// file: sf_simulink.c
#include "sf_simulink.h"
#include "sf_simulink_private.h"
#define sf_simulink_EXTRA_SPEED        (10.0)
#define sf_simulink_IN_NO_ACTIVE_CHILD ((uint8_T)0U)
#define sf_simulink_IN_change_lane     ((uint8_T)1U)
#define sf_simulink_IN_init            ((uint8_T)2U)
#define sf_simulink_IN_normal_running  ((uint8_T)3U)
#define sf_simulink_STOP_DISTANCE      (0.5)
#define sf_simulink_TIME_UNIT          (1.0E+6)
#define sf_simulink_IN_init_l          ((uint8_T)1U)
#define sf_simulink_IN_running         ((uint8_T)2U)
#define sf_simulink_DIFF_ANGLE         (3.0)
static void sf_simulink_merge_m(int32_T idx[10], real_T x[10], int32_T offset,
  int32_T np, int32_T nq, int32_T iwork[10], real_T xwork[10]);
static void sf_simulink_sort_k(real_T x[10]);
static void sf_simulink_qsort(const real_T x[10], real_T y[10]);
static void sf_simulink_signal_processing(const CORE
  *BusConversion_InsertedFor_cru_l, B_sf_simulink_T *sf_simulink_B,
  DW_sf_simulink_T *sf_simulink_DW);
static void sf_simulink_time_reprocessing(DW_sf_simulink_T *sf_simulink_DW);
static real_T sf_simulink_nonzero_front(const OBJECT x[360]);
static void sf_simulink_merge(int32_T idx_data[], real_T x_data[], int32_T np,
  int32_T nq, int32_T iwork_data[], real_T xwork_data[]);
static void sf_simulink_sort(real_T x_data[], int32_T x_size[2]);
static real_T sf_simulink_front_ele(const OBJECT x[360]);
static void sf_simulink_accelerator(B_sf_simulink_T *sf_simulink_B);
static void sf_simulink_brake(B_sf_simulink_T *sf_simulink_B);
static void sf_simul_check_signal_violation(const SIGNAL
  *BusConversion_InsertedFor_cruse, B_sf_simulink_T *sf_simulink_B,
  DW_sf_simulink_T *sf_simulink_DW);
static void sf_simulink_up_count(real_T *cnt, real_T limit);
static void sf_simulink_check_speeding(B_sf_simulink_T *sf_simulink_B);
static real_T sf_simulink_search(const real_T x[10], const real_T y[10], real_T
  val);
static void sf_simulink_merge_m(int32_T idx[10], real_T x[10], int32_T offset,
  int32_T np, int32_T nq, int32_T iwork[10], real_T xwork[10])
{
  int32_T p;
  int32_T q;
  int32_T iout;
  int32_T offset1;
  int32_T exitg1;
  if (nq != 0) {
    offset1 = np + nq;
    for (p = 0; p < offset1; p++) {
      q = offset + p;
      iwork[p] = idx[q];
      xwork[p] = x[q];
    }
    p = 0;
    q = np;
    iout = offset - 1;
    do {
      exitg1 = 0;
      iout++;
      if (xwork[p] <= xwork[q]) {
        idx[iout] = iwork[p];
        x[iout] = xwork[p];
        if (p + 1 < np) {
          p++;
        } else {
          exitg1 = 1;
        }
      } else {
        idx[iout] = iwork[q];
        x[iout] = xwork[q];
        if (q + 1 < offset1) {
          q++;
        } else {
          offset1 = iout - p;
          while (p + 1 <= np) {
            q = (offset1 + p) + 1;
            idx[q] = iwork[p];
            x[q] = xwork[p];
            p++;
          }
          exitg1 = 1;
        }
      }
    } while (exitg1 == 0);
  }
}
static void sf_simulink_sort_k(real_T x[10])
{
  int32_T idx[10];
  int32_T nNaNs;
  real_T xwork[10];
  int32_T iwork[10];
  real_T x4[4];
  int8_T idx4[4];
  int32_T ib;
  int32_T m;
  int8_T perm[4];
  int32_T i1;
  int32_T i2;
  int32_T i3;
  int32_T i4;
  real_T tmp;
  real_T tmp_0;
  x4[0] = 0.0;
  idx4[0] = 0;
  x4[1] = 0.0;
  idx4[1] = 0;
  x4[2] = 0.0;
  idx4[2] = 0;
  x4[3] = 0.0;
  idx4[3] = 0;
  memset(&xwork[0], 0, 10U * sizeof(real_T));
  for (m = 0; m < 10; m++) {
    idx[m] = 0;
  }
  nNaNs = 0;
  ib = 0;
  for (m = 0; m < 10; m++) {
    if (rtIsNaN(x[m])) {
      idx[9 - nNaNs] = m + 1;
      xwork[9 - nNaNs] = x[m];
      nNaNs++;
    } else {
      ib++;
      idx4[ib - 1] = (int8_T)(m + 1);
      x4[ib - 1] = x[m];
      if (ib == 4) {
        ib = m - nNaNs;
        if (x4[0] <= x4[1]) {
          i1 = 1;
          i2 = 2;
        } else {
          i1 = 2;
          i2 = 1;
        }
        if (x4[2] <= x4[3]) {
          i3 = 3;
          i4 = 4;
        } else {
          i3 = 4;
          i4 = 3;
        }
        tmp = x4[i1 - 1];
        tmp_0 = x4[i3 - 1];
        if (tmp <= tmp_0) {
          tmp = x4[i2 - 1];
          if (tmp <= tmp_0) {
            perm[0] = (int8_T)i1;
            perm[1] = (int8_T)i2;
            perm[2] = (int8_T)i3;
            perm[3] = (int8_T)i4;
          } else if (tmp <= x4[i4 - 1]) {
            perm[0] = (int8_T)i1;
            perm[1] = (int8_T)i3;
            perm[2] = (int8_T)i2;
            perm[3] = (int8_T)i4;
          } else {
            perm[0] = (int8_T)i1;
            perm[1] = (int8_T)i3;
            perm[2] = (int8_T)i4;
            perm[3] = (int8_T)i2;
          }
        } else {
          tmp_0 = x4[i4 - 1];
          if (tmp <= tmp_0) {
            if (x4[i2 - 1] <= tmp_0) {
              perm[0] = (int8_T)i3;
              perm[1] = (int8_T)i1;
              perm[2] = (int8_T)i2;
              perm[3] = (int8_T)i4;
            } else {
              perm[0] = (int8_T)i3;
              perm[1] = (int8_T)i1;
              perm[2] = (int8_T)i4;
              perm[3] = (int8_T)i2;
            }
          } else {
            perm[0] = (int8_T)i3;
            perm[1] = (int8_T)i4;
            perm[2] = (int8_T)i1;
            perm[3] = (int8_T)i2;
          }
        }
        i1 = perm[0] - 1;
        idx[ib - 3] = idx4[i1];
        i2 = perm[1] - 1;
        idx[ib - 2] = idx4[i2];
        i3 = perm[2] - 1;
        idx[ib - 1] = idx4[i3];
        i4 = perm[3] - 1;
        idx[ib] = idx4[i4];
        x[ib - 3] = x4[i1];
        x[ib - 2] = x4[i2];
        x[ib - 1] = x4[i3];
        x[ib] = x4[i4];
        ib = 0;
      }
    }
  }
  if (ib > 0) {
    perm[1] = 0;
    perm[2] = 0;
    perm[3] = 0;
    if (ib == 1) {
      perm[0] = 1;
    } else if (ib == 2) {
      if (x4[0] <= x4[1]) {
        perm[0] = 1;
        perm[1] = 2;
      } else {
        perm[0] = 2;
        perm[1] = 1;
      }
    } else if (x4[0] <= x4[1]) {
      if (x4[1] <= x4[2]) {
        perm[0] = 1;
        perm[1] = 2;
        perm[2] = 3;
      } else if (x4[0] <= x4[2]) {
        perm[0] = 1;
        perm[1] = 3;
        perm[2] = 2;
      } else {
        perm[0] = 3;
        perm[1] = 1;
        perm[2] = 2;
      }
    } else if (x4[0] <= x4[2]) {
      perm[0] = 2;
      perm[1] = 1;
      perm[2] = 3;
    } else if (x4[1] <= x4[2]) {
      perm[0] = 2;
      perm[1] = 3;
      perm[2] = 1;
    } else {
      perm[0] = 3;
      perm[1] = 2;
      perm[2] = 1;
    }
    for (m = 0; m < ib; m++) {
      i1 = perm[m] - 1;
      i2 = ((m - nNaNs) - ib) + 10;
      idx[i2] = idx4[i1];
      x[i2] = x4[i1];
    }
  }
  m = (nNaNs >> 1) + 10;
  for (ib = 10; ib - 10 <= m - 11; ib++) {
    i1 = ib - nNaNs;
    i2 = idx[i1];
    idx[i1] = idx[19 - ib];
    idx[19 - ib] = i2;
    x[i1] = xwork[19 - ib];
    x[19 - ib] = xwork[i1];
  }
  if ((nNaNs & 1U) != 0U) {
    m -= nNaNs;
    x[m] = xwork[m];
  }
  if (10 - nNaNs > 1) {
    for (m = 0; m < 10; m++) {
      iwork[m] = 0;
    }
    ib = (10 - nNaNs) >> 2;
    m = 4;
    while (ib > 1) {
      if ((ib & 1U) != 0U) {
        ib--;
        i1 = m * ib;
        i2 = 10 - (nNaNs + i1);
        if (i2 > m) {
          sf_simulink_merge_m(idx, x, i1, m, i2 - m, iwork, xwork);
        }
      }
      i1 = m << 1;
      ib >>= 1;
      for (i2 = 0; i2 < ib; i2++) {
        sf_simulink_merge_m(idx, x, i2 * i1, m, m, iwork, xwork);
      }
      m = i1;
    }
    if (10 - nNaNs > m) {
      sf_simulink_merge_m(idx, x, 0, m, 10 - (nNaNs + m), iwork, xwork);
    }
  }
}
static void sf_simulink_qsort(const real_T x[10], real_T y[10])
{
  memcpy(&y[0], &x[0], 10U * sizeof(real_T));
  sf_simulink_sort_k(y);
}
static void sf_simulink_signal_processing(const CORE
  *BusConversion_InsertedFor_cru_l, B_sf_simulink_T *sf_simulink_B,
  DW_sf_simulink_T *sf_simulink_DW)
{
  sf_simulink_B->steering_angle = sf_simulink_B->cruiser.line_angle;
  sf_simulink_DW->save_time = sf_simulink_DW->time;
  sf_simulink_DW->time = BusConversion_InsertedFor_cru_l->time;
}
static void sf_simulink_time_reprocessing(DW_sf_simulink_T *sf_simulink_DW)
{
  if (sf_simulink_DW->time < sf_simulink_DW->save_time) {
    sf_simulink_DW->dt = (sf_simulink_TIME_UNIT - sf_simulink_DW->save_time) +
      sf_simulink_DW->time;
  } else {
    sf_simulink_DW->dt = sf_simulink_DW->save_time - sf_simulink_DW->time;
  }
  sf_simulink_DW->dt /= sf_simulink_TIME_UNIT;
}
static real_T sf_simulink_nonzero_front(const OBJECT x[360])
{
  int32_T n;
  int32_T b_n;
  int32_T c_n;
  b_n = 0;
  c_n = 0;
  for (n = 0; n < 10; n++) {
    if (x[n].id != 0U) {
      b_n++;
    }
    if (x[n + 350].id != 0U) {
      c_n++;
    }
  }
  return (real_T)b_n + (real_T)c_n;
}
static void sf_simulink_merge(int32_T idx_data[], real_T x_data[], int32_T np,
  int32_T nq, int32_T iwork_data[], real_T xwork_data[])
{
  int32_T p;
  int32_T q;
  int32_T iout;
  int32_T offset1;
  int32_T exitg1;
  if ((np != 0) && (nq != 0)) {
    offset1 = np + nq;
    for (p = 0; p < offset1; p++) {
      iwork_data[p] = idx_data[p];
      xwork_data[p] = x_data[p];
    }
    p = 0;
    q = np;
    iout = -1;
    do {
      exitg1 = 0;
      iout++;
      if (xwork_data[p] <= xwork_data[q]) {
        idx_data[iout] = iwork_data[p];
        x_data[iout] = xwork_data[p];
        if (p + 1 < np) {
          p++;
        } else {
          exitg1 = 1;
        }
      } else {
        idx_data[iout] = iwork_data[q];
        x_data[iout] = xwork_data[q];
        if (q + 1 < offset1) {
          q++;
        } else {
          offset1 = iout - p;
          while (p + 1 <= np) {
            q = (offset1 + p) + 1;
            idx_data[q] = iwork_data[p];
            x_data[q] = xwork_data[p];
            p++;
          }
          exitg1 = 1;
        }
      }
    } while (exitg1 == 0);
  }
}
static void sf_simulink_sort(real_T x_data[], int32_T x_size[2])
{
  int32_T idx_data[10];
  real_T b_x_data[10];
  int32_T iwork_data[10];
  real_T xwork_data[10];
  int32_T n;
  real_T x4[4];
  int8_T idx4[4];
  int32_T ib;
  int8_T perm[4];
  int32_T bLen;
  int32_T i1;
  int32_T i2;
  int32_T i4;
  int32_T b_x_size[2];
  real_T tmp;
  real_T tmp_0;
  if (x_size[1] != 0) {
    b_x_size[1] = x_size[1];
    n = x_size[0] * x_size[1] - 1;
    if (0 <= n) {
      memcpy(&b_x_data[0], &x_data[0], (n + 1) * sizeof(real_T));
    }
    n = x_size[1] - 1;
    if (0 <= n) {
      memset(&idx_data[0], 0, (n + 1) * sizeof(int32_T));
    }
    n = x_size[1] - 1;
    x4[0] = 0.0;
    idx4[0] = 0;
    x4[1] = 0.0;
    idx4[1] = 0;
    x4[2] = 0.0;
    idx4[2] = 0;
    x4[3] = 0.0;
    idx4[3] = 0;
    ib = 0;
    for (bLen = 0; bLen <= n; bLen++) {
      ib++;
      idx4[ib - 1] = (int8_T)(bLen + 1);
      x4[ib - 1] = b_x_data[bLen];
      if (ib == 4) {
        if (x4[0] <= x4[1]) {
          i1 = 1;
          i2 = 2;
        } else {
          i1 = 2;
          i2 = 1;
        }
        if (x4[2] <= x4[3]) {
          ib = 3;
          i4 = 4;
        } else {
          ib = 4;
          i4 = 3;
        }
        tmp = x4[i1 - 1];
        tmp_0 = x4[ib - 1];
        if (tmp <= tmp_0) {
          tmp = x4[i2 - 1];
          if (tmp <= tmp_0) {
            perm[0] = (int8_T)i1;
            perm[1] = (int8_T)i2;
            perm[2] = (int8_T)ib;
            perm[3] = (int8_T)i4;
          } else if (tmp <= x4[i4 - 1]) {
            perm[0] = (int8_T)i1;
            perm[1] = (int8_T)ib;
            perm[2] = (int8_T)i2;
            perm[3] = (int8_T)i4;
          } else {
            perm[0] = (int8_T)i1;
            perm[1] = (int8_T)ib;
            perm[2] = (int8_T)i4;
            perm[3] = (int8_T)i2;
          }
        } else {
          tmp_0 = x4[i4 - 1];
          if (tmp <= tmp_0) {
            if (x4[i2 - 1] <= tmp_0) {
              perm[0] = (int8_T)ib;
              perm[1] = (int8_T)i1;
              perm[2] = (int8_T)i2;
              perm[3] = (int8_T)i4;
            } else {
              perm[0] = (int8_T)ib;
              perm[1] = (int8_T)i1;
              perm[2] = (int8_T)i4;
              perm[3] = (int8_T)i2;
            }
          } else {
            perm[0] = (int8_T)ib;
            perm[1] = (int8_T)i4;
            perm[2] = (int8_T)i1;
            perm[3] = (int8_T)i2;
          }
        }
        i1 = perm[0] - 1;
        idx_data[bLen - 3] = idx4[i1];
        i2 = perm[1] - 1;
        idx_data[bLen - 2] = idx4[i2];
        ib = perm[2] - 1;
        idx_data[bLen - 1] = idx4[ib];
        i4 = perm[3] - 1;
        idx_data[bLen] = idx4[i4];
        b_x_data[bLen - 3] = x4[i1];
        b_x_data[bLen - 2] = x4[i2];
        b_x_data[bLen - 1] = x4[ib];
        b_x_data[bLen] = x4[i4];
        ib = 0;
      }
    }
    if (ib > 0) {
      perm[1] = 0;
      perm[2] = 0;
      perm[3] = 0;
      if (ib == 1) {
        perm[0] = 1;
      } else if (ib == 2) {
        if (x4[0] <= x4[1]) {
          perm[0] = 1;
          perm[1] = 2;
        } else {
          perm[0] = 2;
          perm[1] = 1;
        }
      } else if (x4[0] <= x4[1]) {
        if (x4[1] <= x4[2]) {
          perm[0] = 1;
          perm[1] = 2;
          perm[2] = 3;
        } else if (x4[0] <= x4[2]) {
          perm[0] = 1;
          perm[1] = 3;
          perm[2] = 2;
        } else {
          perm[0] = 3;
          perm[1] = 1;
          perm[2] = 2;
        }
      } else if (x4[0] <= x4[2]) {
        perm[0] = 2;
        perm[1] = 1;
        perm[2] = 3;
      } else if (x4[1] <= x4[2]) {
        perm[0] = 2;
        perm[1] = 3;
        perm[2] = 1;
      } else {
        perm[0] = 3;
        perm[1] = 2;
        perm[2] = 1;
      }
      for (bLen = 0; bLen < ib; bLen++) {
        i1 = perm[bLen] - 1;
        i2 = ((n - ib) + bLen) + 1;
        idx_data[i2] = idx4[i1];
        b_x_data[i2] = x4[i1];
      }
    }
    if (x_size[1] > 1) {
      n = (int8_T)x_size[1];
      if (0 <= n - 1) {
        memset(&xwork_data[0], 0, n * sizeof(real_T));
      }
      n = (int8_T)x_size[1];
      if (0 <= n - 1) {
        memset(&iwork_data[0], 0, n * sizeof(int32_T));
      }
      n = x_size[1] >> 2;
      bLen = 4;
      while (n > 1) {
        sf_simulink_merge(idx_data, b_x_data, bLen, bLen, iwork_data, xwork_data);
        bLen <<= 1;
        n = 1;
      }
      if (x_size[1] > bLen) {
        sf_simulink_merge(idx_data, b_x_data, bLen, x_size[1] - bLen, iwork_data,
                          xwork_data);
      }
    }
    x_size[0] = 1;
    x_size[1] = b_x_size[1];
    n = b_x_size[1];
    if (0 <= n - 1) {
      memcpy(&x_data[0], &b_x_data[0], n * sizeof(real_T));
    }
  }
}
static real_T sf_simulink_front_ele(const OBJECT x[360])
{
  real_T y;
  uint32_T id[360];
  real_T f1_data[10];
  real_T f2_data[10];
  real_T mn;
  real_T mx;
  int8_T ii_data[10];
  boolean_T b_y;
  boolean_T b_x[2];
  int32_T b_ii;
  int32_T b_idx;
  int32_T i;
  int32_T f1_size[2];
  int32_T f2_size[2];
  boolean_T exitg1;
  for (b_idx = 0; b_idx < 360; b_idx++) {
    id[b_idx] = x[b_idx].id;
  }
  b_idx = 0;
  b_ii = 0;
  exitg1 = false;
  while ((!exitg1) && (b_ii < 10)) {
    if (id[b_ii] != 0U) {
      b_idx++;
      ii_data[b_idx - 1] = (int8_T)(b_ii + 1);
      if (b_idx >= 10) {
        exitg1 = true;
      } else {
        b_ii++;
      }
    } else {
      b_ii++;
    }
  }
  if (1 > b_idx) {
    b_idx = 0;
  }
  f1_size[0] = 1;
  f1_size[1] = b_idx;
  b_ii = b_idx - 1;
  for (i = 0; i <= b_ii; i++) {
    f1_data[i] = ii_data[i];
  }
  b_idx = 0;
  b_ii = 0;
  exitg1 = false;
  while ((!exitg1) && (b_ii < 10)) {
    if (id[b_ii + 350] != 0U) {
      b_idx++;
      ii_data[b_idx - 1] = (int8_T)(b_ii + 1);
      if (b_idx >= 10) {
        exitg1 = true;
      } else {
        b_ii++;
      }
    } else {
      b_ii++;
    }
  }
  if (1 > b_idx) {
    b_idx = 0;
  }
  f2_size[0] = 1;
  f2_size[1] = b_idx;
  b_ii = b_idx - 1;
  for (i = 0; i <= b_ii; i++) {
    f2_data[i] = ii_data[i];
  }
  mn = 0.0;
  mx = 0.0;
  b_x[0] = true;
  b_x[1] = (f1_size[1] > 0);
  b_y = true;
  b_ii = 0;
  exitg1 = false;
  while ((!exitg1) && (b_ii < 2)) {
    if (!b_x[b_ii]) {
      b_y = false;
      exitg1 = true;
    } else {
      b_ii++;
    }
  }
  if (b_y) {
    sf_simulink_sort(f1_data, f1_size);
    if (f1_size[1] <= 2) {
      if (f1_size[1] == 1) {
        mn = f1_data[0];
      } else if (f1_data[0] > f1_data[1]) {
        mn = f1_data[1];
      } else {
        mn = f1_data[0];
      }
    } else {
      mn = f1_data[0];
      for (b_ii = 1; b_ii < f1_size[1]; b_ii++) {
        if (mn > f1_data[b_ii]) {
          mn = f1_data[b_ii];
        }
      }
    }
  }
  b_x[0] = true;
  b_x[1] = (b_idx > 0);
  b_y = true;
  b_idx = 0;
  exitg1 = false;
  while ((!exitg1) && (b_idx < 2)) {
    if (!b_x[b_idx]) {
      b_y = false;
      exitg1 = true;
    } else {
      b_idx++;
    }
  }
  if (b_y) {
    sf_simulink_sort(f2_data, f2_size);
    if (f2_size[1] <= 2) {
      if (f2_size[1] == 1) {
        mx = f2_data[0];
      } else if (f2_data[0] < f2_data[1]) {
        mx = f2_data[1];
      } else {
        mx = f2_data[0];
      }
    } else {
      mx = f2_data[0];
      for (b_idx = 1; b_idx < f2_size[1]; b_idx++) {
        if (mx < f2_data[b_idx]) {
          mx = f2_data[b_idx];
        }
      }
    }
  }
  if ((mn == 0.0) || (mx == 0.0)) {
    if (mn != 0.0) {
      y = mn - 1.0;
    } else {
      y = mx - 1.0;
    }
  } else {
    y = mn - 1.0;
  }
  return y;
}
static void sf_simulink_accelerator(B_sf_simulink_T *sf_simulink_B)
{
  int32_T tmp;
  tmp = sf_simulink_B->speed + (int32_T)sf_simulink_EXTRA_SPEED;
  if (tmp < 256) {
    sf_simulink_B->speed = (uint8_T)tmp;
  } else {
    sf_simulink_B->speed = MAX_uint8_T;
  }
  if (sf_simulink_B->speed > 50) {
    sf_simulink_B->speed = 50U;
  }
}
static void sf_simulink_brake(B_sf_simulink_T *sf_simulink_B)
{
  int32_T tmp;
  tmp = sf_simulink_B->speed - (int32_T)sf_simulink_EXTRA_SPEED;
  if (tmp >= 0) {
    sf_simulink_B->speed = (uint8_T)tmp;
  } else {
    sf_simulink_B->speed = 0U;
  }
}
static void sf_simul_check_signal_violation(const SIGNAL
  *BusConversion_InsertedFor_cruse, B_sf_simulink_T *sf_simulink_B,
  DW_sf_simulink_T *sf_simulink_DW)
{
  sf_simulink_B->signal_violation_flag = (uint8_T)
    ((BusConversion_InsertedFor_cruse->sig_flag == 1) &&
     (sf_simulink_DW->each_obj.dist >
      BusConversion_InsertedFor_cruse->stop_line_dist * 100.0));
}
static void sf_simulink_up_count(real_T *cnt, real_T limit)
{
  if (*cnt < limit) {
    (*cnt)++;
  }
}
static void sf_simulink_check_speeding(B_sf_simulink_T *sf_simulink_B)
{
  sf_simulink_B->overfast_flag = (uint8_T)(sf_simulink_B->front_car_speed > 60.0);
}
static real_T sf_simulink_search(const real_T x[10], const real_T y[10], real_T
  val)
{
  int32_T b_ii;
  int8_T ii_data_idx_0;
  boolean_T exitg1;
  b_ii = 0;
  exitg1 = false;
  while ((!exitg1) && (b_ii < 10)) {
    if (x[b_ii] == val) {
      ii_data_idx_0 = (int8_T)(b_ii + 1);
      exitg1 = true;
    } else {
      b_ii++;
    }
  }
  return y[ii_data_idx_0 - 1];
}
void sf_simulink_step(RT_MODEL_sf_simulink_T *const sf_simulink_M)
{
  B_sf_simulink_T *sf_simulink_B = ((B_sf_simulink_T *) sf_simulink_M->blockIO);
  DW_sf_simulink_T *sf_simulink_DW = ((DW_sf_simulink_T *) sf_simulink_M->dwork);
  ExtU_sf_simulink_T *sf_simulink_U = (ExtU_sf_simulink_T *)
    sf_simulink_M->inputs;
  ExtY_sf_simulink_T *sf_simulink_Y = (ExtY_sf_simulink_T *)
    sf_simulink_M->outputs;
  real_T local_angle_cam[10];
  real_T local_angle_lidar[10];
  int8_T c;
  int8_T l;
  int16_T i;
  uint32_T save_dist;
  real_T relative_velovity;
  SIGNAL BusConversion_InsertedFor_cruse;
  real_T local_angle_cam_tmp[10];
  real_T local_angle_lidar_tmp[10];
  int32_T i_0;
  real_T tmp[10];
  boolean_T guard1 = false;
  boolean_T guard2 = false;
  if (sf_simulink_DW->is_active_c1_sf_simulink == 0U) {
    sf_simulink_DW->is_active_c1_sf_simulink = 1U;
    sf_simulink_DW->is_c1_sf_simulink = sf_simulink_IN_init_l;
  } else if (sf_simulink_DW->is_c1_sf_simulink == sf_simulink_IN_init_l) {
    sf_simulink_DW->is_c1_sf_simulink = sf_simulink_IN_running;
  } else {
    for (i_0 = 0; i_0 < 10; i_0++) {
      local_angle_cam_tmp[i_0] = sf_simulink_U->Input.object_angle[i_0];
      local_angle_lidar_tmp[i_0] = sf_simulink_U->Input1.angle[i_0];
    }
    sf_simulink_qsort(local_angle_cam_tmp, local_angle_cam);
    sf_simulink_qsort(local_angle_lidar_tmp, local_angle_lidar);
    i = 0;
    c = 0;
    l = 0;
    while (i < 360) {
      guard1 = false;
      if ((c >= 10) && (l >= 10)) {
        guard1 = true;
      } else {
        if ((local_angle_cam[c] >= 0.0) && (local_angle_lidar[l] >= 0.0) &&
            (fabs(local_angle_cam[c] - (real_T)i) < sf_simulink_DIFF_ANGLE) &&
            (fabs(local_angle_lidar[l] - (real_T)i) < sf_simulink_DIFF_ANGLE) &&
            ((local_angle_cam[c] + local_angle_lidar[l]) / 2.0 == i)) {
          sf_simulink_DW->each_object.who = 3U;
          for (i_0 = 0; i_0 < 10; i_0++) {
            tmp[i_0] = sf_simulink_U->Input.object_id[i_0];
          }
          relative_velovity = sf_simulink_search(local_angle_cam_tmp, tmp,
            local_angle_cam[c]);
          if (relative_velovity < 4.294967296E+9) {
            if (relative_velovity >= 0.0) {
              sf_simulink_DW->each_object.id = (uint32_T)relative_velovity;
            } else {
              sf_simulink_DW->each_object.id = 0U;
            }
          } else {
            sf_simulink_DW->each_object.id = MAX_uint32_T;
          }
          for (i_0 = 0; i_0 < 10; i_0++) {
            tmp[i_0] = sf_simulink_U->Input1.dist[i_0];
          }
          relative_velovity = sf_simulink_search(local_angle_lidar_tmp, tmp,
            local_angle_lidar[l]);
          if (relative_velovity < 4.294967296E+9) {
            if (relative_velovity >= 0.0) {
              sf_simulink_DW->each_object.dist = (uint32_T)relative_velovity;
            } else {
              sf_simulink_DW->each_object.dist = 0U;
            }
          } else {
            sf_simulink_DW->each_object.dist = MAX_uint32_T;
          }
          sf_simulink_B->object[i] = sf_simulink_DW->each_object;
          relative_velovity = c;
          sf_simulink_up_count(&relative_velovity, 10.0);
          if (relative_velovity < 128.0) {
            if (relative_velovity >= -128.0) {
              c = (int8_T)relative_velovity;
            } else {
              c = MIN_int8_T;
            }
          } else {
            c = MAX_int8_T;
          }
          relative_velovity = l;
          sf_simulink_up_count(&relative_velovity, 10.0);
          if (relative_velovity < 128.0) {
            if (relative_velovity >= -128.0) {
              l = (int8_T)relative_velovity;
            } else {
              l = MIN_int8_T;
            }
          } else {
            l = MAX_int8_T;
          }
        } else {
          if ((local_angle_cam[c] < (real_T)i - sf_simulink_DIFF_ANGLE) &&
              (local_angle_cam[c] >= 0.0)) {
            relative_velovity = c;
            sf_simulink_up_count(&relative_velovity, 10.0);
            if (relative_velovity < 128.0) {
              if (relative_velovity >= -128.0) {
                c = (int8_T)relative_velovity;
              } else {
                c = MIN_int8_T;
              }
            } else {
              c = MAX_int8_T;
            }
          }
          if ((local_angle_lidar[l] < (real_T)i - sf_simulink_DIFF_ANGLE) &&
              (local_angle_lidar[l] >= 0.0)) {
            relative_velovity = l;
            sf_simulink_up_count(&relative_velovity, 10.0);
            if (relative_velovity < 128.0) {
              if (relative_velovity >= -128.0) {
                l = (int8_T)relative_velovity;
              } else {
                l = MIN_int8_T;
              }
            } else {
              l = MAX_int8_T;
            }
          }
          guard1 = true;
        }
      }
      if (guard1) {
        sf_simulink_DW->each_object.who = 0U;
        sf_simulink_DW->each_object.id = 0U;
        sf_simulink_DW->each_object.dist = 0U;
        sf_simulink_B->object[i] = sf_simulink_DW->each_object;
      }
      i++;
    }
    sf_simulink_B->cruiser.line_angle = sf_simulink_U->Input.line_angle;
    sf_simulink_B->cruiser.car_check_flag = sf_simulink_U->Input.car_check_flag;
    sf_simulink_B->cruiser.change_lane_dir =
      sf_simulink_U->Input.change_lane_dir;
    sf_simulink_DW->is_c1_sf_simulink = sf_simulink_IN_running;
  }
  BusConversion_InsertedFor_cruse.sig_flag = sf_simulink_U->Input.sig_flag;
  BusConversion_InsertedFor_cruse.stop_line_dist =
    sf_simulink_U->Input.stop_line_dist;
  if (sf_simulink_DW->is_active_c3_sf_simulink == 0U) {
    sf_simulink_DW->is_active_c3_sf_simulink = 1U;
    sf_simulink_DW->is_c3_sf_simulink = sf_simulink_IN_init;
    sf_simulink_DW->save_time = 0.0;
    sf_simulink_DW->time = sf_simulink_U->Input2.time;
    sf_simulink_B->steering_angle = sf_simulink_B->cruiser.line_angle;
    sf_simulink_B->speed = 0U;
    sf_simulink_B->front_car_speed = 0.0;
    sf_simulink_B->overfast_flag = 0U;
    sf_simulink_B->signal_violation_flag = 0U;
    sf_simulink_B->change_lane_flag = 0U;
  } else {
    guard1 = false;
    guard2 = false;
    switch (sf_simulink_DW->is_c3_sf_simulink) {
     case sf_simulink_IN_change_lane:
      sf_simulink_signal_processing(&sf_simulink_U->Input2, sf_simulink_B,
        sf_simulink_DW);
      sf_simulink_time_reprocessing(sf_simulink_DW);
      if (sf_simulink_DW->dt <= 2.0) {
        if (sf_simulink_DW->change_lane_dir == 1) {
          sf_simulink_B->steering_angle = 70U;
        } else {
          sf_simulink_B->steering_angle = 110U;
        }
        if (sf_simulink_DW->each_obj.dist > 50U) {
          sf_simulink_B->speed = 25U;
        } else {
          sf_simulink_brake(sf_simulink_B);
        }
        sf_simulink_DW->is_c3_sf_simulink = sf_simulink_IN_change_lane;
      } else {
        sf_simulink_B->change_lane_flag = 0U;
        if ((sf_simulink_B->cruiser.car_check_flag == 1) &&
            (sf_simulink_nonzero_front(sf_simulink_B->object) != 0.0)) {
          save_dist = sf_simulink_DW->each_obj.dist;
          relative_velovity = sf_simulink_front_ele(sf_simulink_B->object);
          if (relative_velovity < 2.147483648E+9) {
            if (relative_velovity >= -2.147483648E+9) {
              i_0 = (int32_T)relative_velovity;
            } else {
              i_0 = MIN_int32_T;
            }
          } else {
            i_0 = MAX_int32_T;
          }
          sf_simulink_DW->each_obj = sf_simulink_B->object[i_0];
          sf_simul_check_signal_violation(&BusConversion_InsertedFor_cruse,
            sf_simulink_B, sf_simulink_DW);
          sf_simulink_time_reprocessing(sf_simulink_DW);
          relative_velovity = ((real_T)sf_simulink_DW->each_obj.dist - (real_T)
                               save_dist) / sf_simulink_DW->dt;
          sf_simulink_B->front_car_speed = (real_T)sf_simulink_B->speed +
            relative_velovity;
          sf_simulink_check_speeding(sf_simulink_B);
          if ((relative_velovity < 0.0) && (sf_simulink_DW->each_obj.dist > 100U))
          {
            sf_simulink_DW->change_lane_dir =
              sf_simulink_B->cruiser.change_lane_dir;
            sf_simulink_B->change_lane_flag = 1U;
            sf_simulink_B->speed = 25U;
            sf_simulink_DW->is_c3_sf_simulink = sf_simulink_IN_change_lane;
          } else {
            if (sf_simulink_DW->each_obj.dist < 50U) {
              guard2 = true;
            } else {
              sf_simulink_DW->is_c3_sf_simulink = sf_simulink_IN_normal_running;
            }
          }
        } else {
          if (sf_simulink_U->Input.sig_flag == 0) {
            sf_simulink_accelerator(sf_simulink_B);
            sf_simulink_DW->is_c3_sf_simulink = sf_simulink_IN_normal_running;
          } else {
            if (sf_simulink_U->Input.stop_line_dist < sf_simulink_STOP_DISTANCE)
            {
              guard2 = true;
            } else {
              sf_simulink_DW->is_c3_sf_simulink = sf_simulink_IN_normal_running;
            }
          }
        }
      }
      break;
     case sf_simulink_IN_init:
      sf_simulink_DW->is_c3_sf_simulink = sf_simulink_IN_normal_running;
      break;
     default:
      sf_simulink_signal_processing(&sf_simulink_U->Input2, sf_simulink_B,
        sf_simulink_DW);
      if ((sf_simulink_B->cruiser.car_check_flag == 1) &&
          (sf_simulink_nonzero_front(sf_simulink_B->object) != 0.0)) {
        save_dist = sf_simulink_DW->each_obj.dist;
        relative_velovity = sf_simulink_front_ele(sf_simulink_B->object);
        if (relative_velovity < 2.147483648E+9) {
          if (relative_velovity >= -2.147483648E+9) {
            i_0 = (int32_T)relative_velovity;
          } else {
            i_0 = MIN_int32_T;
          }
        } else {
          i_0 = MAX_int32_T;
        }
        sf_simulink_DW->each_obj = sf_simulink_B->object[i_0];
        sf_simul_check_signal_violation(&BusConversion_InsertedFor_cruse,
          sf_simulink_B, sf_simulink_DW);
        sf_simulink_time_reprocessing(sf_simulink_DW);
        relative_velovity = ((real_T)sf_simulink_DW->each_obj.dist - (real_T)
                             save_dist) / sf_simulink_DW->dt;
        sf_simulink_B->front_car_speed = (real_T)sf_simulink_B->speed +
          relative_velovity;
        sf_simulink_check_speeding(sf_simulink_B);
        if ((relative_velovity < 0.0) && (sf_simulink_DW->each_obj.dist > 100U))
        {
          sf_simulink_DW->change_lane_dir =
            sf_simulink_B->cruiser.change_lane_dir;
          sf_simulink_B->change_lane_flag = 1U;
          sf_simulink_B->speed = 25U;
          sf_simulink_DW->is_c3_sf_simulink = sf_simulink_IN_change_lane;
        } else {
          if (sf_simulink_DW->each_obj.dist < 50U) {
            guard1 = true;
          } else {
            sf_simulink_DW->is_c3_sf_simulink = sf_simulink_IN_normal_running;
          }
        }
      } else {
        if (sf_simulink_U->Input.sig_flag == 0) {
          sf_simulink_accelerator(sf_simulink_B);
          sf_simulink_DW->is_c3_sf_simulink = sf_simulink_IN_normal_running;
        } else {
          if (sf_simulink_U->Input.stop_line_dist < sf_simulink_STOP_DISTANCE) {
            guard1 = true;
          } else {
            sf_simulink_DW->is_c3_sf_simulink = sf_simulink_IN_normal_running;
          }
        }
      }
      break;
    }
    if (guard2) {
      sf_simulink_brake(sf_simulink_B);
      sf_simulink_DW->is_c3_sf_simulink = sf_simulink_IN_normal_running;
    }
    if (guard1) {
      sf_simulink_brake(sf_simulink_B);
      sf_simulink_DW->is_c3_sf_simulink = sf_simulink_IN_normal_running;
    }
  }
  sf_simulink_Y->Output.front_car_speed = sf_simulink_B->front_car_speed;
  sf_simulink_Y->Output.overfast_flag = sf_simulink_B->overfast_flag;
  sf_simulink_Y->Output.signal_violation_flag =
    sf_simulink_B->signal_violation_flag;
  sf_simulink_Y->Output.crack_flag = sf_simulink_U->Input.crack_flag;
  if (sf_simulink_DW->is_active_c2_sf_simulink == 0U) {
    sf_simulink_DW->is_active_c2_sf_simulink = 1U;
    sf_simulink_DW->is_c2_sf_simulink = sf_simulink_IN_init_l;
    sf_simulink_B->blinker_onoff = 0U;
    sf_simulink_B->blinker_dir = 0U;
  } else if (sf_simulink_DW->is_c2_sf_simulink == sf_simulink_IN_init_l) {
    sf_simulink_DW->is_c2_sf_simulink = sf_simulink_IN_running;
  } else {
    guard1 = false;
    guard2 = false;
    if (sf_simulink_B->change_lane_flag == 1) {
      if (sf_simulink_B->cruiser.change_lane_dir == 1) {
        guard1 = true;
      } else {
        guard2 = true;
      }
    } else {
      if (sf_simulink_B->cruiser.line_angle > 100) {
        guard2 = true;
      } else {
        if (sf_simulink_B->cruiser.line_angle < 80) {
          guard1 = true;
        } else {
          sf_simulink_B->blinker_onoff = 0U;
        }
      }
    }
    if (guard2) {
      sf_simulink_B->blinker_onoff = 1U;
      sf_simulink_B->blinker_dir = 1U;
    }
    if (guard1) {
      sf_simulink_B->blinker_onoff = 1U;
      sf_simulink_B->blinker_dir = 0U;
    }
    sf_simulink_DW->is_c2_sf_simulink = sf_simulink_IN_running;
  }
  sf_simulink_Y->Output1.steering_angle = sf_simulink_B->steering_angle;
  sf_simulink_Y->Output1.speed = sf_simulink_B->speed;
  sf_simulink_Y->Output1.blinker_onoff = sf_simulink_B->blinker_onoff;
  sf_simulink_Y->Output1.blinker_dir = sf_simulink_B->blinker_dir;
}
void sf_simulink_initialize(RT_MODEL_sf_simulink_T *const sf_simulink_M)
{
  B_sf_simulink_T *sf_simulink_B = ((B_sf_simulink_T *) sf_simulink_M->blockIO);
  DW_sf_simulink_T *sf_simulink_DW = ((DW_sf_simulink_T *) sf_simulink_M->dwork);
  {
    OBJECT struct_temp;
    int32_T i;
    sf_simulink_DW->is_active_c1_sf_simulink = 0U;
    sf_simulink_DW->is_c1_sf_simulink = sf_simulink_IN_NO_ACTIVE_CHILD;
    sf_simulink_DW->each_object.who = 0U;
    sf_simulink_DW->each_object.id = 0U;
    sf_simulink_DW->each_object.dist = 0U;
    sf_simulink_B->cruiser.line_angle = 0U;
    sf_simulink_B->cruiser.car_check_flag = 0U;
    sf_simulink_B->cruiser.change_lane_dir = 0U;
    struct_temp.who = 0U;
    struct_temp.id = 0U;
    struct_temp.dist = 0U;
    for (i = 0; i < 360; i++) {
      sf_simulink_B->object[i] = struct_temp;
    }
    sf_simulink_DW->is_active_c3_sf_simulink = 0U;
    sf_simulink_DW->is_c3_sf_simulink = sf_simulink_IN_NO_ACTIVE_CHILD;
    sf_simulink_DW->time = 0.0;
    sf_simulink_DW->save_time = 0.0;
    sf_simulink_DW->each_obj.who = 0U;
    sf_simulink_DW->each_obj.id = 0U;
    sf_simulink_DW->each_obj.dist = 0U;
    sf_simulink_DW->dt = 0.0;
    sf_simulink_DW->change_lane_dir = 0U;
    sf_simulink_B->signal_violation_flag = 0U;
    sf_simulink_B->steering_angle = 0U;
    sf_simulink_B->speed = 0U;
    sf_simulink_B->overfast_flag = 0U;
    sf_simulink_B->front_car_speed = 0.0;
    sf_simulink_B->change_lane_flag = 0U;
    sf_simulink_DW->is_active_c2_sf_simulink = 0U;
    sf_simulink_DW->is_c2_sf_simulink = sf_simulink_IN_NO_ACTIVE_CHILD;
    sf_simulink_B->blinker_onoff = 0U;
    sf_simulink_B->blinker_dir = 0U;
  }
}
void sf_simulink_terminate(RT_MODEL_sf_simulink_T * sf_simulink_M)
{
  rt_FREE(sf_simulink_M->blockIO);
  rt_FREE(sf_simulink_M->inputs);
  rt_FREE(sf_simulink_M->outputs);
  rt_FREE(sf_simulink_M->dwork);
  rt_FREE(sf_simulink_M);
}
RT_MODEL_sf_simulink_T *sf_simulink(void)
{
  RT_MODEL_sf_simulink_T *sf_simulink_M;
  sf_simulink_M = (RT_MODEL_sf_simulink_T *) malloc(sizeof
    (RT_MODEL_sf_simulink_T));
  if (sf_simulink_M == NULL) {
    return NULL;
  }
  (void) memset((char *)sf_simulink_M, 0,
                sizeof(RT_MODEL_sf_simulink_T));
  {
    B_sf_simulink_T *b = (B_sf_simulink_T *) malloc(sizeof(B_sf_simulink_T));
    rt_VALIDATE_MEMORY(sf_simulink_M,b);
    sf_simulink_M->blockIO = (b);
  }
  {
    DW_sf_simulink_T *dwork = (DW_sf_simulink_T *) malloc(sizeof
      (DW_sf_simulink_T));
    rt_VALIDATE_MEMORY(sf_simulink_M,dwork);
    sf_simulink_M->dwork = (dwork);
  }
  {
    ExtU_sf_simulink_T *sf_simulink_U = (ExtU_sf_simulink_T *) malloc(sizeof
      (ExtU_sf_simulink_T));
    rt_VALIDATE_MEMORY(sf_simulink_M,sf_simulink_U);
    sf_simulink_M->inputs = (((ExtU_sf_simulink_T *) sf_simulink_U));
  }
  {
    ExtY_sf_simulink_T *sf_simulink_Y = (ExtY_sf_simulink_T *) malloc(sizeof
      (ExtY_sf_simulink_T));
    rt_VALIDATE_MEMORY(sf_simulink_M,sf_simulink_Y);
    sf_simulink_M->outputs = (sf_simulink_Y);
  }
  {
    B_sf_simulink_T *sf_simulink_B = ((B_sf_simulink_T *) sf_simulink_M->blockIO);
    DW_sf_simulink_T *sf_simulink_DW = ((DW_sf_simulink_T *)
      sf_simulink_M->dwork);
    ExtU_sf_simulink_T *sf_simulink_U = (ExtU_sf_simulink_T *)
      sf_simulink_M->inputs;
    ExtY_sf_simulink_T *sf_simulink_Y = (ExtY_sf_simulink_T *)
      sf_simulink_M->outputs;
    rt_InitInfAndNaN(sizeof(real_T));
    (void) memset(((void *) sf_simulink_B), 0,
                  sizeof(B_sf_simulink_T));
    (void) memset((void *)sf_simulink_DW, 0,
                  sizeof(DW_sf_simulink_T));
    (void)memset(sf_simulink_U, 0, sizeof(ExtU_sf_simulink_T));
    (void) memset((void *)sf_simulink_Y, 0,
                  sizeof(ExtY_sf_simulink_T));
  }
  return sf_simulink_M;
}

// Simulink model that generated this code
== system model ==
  Input : Inport
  Input1 : Inport
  Input2 : Inport
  Output : Outport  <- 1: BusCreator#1
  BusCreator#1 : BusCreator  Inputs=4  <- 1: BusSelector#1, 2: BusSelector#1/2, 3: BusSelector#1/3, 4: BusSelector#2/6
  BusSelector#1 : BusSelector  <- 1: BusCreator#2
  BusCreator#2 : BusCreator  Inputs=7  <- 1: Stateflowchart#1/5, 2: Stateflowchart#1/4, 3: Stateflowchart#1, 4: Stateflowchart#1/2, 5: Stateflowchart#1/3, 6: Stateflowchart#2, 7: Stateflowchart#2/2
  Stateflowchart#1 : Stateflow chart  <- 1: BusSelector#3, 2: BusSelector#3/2, 3: Input2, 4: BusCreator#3
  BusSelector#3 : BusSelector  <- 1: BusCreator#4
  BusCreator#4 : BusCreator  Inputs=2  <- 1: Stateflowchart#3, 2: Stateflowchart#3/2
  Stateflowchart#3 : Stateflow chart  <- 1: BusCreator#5, 2: Input1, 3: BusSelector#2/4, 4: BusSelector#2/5
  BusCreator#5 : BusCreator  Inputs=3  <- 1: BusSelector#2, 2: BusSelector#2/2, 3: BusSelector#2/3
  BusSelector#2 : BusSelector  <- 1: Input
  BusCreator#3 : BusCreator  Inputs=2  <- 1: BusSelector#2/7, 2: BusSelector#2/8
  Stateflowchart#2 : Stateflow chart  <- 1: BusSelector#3, 2: Stateflowchart#1/6
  Output1 : Outport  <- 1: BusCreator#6
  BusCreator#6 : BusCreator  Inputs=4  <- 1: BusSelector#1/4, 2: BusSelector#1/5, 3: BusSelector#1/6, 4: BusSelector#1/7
== stateflow chart Stateflowchart#3 ==
  state cnt = up_count(cnt, limit) [function]
    (default) -> (junction 136)
    (junction 136) -> (junction 125) [order 1] : [cnt < limit]
        | {cnt = cnt + 1;}
    (junction 131) -> (junction 125)
    (junction 125) -> (junction 133)
    (junction 136) -> (junction 131) [order 2]
  state init
    local_angle_cam = -1;
    local_angle_lidar = -1;
  state running
  (default) -> init
  init -> running
  (junction 99) -> running
  (junction 95) -> (junction 99)
  running -> (junction 180) : /* local data qsort */
      | {
      | local_angle_cam = qsort(cam.object_angle);
      | local_angle_lidar = qsort(lidar.angle);
      | }
  (junction 180) -> (junction 37) : {i = 0; c = 0; l = 0;}
  (junction 227) -> (junction 36) [order 2]
  (junction 36) -> (junction 105) [order 1] : /* each data is bigger than zero,
      | the absolute value of diff between local angles is smaller than three.
      | !!! used data is set minus one !!!
      | data is existed, what... */
      | [
      | local_angle_cam[c] >= 0 && local_angle_lidar[l] >= 0 && ...
      | abs(local_angle_cam[c] - i) < DIFF_ANGLE && ...
      | abs(local_angle_lidar[l] - i) < DIFF_ANGLE && ...
      | (local_angle_cam[c] + local_angle_lidar[l]) / 2 == i
      | ]
  (junction 37) -> (junction 227) [order 1] : [i < 360]
  (junction 227) -> (junction 232) [order 1] : [c >= 10 && l >= 10]
  (junction 36) -> (junction 196) [order 2]
  (junction 105) -> (junction 143) : {
      | each_object.who = 3;
      | each_object.id = search(cam.object_angle, cam.object_id, local_angle_cam[c]);
      | each_object.dist = search(lidar.angle, lidar.dist, local_angle_lidar[l]);
      | object[i] = each_object;
      |
      | c = up_count(c, 10);
      | l = up_count(l, 10);
      | }
  (junction 39) -> (junction 37)
  (junction 37) -> (junction 40) [order 2] : /* data fetch*/
      | {
      | cruiser.line_angle = line_angle;
      | cruiser.car_check_flag = car_check_flag;
      | cruiser.change_lane_dir = cam.change_lane_dir;
      | }
  (junction 196) -> (junction 241) [order 1] : [local_angle_cam[c] < i - DIFF_ANGLE && local_angle_cam[c] >= 0]
      | {c = up_count(c, 10);}
  (junction 196) -> (junction 239) [order 2]
  (junction 241) -> (junction 203)
  (junction 203) -> (junction 239)
  (junction 239) -> (junction 207)
  (junction 207) -> (junction 236) [order 1] : [local_angle_lidar[l] < i - DIFF_ANGLE && local_angle_lidar[l] >= 0]
      | {l = up_count(l, 10);}
  (junction 207) -> (junction 232) [order 2]
  (junction 236) -> (junction 205)
  (junction 205) -> (junction 232)
  (junction 232) -> (junction 38) : {
      | each_object.who = 0;
      | each_object.id = 0;
      | each_object.dist = 0;
      | object[i] = each_object;
      | }
  (junction 40) -> (junction 95)
  (junction 38) -> (junction 39) : {i = i + 1;}
  (junction 143) -> (junction 38)
  data: cnt function_input double; limit function_input double; cnt function_output double; x function_input double size=10; y function_output double size=10; x function_input double size=10; y function_input double size=10; ret function_output double; val function_input double; cam input Bus: C_BUS; lidar input Bus: LIDAR; cruiser output Bus: CRUISER size=1; line_angle input; local_angle_cam local double size=10; local_angle_lidar local double size=10; car_check_flag input; c local int8; l local int8; i local int16; object output Bus: OBJECT size=360; each_object local Bus: OBJECT; DIFF_ANGLE constant double =3
  function y = qsort(x):
    | function y = qsort(x)
    | input = zeros(1,10);
    | for n = 1:10
    |     input(n) = x(n);
    | end
    | input = sort(input);
    | for n = 1:10
    |     y(n) = input(n);
    | end
  function ret = search(x, y, val):
    | function ret = search(x, y, val)
    | ind = find(x == val, 1);
    | ret = y(ind(1));

== stateflow chart Stateflowchart#2 ==
  state init
    blinker_onoff = 0;
    blinker_dir = 0;
  state running
  (default) -> init
  init -> running
  (junction 32) -> running
  (junction 30) -> (junction 32)
  running -> (junction 17)
  (junction 17) -> (junction 19) [order 1] : /* lane change or not */
      | [change_lane_flag == 1]
  (junction 19) -> (junction 41) [order 1] : [cruiser.change_lane_dir == 1]
  (junction 17) -> (junction 21) [order 2]
  (junction 19) -> (junction 45) [order 2]
  (junction 41) -> (junction 46)
  (junction 21) -> (junction 45) [order 1] : /* turn left */
      | [cruiser.line_angle > ANGLE_STD + 10]
  (junction 21) -> (junction 35) [order 2]
  (junction 45) -> (junction 49) : {blinker_onoff = 1;
      | blinker_dir = 1;}
  (junction 35) -> (junction 46) [order 1] : /* turn right */
      | [cruiser.line_angle < ANGLE_STD - 10]
  (junction 35) -> (junction 28) [order 2] : {blinker_onoff = 0;}
  (junction 46) -> (junction 38) : {blinker_onoff = 1;
      | blinker_dir = 0;}
  (junction 28) -> (junction 30)
  (junction 49) -> (junction 28)
  (junction 38) -> (junction 49)
  data: cruiser input Bus: CRUISER; blinker_onoff output uint8; blinker_dir output uint8; change_lane_flag input; ANGLE_STD constant double =90

== stateflow chart Stateflowchart#1 ==
  state signal_processing [function]
    (default) -> (junction 977)
    (junction 977) -> (junction 965) [order 1] : % yellow or red signal
        | [signal.sig_flag == 1]
    (junction 977) -> (junction 969) [order 2]
    (junction 965) -> (junction 969) [order 2]
    (junction 969) -> (junction 971) : {move_f = 1;}
    (junction 965) -> (junction 970) [order 1] : [signal.stop_line_dist < STOP_DISTANCE]
        | {move_f = 0;}
    (junction 970) -> (junction 971)
    (junction 971) -> (junction 966) : {
        | steering_angle = cruiser.line_angle;
        | save_time = time;
        | time = bus_time.time;
        | }
  state init
    %local
    move_f = 0;
    save_dist = 0;
    save_time = 0;
    time = bus_time.time;
    %output
    steering_angle = cruiser.line_angle;
    speed = 0;
    front_car_speed = 0;
    overfast_flag = 0;
    signal_violation_flag = 0;
    change_lane_flag = 0;
  state normal_running
  state time_reprocessing [function]
    (default) -> (junction 997)
    (junction 997) -> (junction 1001) [order 1] : /* time is mircoseconds.
        | range is 0 ~ 999999*/
        | [time < save_time]
        | {dt = TIME_UNIT - save_time + time;}
    (junction 997) -> (junction 999) [order 2] : {dt = save_time - time;}
    (junction 1001) -> (junction 1003)
    (junction 1003) -> (junction 999)
    (junction 999) -> (junction 1005) : {dt = dt / TIME_UNIT;}
  state check_speeding [function]
    (default) -> (junction 1058)
    (junction 1058) -> (junction 1059) [order 1] : /* overfast checking */
        | [front_car_speed > 60]
        | {overfast_flag = 1;}
    (junction 1058) -> (junction 1064) [order 2]
    (junction 1059) -> (junction 1063)
    (junction 1064) -> (junction 1063) : {overfast_flag = 0;}
  state accelerator [function]
    (default) -> (junction 1024) : {speed += EXTRA_SPEED;}
    (junction 1024) -> (junction 1022) : [speed > 50]
        | {speed = 50;}
  state brake [function]
    (default) -> (junction 1030) : {speed -= EXTRA_SPEED;}
    (junction 1030) -> (junction 1027) : [speed < 0]
        | {speed = 0;}
  state change_lane
  state check_signal_violation [function]
    (default) -> (junction 1127)
    (junction 1127) -> (junction 1129) [order 1] : [signal.sig_flag == 1 && each_obj.dist > (signal.stop_line_dist*100)]
        | {signal_violation_flag = 1;}
    (junction 1127) -> (junction 1139) [order 2] : {signal_violation_flag = 0;}
    (junction 1129) -> (junction 1141)
    (junction 1141) -> (junction 1139)
  (default) -> init
  (junction 599) -> normal_running
  init -> normal_running
  (junction 595) -> (junction 599)
  normal_running -> (junction 562) : {signal_processing();}
  (junction 562) -> (junction 564) [order 2] : /* undiscover the car in front */
  (junction 1123) -> (junction 562) : {change_lane_flag = 0;}
  (junction 1114) -> (junction 1116) : {steering_angle = 110;}
  (junction 564) -> (junction 571)
  (junction 562) -> (junction 1066) [order 1] : /* discover the car in front */
      | [cruiser.car_check_flag == 1 && nonzero_front(object) != 0]
      | {
      | car_num = front_ele(object);
      | save_dist = each_obj.dist;
      | each_obj = object[car_num];
      |
      | check_signal_violation();
      |
      | time_reprocessing();
      | relative_velovity = (each_obj.dist - save_dist) / dt;
      |
      | /* speed unit and relative_velovity unit is centimeters per seconds */
      | front_car_speed = speed + relative_velovity;
      | check_speeding();
      | }
  (junction 1103) -> (junction 1123) [order 2]
  (junction 1112) -> (junction 1114) [order 2]
  (junction 1116) -> (junction 1108)
  (junction 1103) -> (junction 1112) [order 1] : [dt <= 2]
  (junction 1112) -> (junction 1108) [order 1] : [change_lane_dir == 1]
      | {steering_angle = 70;}
  change_lane -> (junction 1103) : {signal_processing();
      | time_reprocessing();}
  (junction 1108) -> (junction 1109)
  (junction 1066) -> change_lane [order 1] : /* the front car is getting closer
      | If the front car is already close, can't change lane */
      | [relative_velovity < 0 && each_obj.dist > 100]
      | {
      | change_lane_dir = cruiser.change_lane_dir;
      | change_lane_flag = 1;
      | speed = 25;
      | }
  (junction 1136) -> change_lane
  (junction 1109) -> (junction 1136) [order 1] : [each_obj.dist > 50]
      | {speed = 25;}
  (junction 1066) -> (junction 575) [order 2]
  (junction 1133) -> (junction 1136)
  (junction 1109) -> (junction 1131) [order 2]
  (junction 571) -> (junction 1012) [order 1] : /* signal light color isn't yellow or red */
      | [signal.sig_flag == 0]
  (junction 1012) -> (junction 1015) : {accelerator();}
  (junction 571) -> (junction 1031) [order 2]
  (junction 1131) -> (junction 1133) : {brake();}
  (junction 1031) -> (junction 1035) [order 1] : /* stop line is close */
      | [signal.stop_line_dist < STOP_DISTANCE]
  (junction 1035) -> (junction 1045)
  (junction 1031) -> (junction 629) [order 2]
  (junction 575) -> (junction 1045) [order 1] : /* the front car is close
      | if it insisted accelerate*/
      | [each_obj.dist < 50]
  (junction 1045) -> (junction 1037) : {brake();}
  (junction 575) -> (junction 1077) [order 2]
  (junction 1015) -> (junction 1037)
  (junction 1037) -> (junction 629)
  (junction 629) -> (junction 1077)
  (junction 1077) -> (junction 595)
  data: x function_input Bus: OBJECT size=360; y function_output double; x function_input Bus: OBJECT size=360; y function_output double; signal_violation_flag output uint8; cruiser input Bus: CRUISER; object input Bus: OBJECT size=360; steering_angle output uint8; speed output uint8; bus_time input Bus: CORE; overfast_flag output uint8; front_car_speed output double; time local double; save_time local double; save_dist local double; signal input Bus: SIGNAL; move_f local double; car_num local double; each_obj local Bus: OBJECT; relative_velovity local double; dt local double; TIME_UNIT constant double =1000000; EXTRA_SPEED constant double =10; STOP_DISTANCE constant double =0.5; change_lane_dir local uint8; change_lane_flag output uint8
  function y = nonzero_front(x):
    | function y = nonzero_front(x)
    | id1 = zeros(1,10);
    | id2 = zeros(1,10);
    | for n = 1:10
    |     id1(n) = x(n).id;
    |     id2(n) = x(n + 350).id;
    | end
    | y = nnz(id1) + nnz(id2);
  function y = front_ele(x):
    | function y = front_ele(x)
    | id = zeros(1,360);
    | for n = 1:360
    |     id(n) = x(n).id;
    | end
    | f1 = find(id(1:10));
    | f2 = find(id(351:360));
    | mn = 0;   mx = 0;
    | if size(f1) > 0
    |     f1 = sort(f1);
    |     mn = min(f1);
    | end
    | if size(f2) > 0
    |     f2 = sort(f2);
    |     mx = max(f2); 
    | end
    | if mn == 0 || mx == 0
    |     if mn ~= 0
    |         y = mn - 1;
    |     else
    |         y = mx - 1;  
    |     end
    | elseif mn > abs(mx - 360)
    |     y = mx - 1;
    | else
    |     y = mn - 1;
    | end
